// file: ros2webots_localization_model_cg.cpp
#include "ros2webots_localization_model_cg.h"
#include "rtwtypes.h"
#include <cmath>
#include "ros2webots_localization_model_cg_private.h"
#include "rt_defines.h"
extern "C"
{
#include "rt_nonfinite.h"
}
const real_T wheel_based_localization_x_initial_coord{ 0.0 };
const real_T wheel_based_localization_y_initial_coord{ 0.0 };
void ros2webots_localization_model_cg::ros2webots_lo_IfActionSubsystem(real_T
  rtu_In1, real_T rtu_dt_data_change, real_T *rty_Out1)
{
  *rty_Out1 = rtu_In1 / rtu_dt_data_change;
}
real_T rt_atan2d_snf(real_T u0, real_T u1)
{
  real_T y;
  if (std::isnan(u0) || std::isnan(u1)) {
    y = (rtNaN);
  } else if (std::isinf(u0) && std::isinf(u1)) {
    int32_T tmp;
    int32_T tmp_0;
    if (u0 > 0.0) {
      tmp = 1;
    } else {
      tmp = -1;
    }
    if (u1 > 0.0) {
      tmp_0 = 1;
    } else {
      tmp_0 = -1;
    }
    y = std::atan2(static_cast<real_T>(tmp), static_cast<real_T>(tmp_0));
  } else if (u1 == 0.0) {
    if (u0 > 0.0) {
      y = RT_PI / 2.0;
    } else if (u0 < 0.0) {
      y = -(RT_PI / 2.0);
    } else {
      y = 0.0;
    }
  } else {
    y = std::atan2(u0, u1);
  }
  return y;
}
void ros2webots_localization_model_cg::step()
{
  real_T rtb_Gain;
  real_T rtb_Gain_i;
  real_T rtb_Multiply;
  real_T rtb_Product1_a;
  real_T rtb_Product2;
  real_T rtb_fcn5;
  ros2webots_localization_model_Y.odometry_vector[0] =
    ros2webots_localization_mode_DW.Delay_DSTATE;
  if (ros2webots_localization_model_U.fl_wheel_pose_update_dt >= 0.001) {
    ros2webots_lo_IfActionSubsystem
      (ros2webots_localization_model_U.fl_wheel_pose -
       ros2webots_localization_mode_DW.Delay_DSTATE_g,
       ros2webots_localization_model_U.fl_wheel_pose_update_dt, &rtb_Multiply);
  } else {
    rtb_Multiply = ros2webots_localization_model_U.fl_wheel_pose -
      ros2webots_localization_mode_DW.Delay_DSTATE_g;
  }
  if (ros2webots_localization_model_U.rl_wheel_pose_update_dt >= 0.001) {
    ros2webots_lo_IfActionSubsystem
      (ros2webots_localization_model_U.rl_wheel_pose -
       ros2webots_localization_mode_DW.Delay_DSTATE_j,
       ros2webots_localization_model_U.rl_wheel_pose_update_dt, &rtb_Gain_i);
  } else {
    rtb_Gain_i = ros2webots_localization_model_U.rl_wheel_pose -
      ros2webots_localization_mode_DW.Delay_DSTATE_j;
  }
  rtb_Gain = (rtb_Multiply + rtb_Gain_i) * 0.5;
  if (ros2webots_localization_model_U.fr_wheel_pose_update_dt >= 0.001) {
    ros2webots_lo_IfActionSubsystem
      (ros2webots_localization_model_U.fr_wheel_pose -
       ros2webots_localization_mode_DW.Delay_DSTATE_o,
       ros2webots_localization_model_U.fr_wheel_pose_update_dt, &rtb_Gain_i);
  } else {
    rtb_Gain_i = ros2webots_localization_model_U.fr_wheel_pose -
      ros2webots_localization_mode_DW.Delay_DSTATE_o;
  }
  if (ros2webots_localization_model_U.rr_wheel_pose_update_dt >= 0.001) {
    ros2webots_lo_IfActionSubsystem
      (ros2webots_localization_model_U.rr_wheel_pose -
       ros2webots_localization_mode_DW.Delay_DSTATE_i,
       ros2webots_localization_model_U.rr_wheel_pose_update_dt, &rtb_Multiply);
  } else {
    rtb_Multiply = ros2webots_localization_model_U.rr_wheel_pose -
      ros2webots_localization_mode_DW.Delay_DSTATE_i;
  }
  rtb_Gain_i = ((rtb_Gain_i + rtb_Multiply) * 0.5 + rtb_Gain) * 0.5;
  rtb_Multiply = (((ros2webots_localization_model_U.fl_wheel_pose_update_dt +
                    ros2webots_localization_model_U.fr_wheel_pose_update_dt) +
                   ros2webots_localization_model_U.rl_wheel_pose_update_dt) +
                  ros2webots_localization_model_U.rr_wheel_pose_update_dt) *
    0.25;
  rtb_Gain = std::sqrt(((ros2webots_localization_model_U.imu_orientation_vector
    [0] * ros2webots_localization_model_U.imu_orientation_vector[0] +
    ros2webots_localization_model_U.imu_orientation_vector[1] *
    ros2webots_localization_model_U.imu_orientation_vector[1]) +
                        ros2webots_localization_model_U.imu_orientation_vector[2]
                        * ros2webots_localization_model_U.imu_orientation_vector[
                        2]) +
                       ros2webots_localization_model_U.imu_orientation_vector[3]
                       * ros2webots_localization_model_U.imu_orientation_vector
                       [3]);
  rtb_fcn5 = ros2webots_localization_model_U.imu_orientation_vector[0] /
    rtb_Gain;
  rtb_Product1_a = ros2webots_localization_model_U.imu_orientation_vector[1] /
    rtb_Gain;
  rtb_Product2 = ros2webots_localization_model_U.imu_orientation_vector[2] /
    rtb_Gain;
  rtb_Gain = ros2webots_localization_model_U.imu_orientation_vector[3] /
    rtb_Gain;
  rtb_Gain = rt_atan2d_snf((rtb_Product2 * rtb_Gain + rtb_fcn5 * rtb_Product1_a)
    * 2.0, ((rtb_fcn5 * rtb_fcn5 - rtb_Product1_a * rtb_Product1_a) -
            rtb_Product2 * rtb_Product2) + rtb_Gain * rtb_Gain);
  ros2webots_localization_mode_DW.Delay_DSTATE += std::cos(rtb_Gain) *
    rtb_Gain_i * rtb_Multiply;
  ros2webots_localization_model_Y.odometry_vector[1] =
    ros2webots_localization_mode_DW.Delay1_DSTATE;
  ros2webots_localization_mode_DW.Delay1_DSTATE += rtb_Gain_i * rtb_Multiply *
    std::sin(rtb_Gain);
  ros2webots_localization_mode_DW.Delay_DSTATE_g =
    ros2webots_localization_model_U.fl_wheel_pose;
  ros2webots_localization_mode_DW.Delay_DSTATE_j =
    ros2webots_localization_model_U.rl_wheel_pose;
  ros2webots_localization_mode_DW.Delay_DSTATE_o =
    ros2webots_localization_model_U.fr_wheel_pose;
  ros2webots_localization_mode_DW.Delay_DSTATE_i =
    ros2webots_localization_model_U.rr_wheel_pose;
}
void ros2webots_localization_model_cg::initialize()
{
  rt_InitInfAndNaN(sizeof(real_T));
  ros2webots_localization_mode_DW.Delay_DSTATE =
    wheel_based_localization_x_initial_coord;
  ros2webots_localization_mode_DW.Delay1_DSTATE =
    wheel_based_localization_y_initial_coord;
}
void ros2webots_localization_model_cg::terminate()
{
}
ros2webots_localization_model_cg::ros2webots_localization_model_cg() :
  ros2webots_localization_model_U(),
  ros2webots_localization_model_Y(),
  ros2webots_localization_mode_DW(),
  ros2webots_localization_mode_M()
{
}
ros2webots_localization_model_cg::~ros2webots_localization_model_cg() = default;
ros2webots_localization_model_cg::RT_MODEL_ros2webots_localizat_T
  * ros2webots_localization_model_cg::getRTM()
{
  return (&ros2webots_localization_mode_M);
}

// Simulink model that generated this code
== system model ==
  imu_orientation_vector : Inport
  Inport#1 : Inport
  Inport#2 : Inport
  fl_wheel_pose : Inport
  fr_wheel_pose : Inport
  rl_wheel_pose : Inport
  rr_wheel_pose : Inport
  fl_wheel_pose_update_dt : Inport
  fr_wheel_pose_update_dt : Inport
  rl_wheel_pose_update_dt : Inport
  rr_wheel_pose_update_dt : Inport
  odometry_vector : Outport  <- 1: Concatenate#1
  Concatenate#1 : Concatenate  <- 1: Delay, 2: Delay1
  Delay : Delay  DelayLength=1  InitialCondition=wheel_based_localization_x_initial_coord  <- 1: Sum#1
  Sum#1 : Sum  Inputs=++  <- 1: Product#1, 2: Delay
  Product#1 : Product  Inputs=3  <- 1: Trigonometry#1, 2: Gain, 3: Multiply
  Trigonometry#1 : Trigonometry  Operator=cos  <- 1: Selector#1
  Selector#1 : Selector  Indices=3  <- 1: QuaternionstoRotationAngles#1
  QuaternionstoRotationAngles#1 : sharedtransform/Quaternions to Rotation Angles  <- 1: Concatenate#2
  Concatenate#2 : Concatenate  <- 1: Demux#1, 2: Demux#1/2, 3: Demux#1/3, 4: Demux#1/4
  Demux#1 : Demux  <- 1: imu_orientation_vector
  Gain : Gain  Gain=1/2  <- 1: Sum#2
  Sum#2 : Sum  Inputs=++  <- 1: Gain#1, 2: Gain#2
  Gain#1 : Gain  Gain=1/2  <- 1: Sum#3
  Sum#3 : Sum  Inputs=++  <- 1: Merge#1, 2: Merge#2
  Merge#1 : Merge  <- 1: IfActionSubsystem, 2: Subsystem#1
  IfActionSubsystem : Subsystem  <- 1: Sum#4, 2: fl_wheel_pose_update_dt, Action: If#1
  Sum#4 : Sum  Inputs=+-  <- 1: fl_wheel_pose, 2: Delay#1
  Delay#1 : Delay  DelayLength=1  <- 1: fl_wheel_pose
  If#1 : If  IfExpression=u1 >= manual_derivative_dt_threshold  <- 1: fl_wheel_pose_update_dt
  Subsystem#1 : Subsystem  <- 1: Sum#4, Action: If#1/2
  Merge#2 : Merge  <- 1: Subsystem#2, 2: Subsystem#3
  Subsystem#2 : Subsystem  <- 1: Sum#5, 2: rl_wheel_pose_update_dt, Action: If#2
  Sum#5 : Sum  Inputs=+-  <- 1: rl_wheel_pose, 2: Delay#2
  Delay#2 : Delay  DelayLength=1  <- 1: rl_wheel_pose
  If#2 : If  IfExpression=u1 >= manual_derivative_dt_threshold  <- 1: rl_wheel_pose_update_dt
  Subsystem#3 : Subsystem  <- 1: Sum#5, Action: If#2/2
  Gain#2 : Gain  Gain=1/2  <- 1: Sum#6
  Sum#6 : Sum  Inputs=++  <- 1: Merge#3, 2: Merge#4
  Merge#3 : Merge  <- 1: Subsystem#4, 2: Subsystem#5
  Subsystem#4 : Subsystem  <- 1: Sum#7, 2: fr_wheel_pose_update_dt, Action: If#3
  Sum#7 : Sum  Inputs=+-  <- 1: fr_wheel_pose, 2: Delay#3
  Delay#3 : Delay  DelayLength=1  <- 1: fr_wheel_pose
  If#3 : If  IfExpression=u1 >= manual_derivative_dt_threshold  <- 1: fr_wheel_pose_update_dt
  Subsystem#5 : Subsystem  <- 1: Sum#7, Action: If#3/2
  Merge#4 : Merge  <- 1: Subsystem#6, 2: Subsystem#7
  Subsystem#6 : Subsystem  <- 1: Sum#8, 2: rr_wheel_pose_update_dt, Action: If#4
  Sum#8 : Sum  Inputs=+-  <- 1: rr_wheel_pose, 2: Delay#4
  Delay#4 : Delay  DelayLength=1  <- 1: rr_wheel_pose
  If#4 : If  IfExpression=u1 >= manual_derivative_dt_threshold  <- 1: rr_wheel_pose_update_dt
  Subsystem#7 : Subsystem  <- 1: Sum#8, Action: If#4/2
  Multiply : Gain  Gain=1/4  <- 1: Sum#9
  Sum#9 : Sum  Inputs=++++  <- 1: fl_wheel_pose_update_dt, 2: fr_wheel_pose_update_dt, 3: rl_wheel_pose_update_dt, 4: rr_wheel_pose_update_dt
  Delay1 : Delay  DelayLength=1  InitialCondition=wheel_based_localization_y_initial_coord  <- 1: Sum#10
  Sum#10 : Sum  Inputs=++  <- 1: Product1, 2: Delay1
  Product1 : Product  Inputs=3  <- 1: Gain, 2: Multiply, 3: Trigonometry#2
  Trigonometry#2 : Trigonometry  <- 1: Selector#1
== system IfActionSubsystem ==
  In1 : Inport
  dt_data_change : Inport
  ActionPort#1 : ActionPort
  Out1 : Outport  <- 1: Product#2
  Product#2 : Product  Inputs=*/  <- 1: In1, 2: dt_data_change
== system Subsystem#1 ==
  Inport#3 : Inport
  ActionPort#2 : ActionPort
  Outport#1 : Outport  <- 1: Inport#3
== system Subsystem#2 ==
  Inport#4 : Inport
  Inport#5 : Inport
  ActionPort#3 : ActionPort
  Outport#2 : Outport  <- 1: Product#3
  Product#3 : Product  Inputs=*/  <- 1: Inport#4, 2: Inport#5
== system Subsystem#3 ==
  Inport#6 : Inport
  ActionPort#4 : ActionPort
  Outport#3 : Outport  <- 1: Inport#6
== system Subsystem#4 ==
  Inport#7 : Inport
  Inport#8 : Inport
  ActionPort#5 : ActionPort
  Outport#4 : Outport  <- 1: Product#4
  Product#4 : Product  Inputs=*/  <- 1: Inport#7, 2: Inport#8
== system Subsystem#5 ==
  Inport#9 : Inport
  ActionPort#6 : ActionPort
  Outport#5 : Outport  <- 1: Inport#9
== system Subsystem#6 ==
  Inport#10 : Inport
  Inport#11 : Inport
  ActionPort#7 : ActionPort
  Outport#6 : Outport  <- 1: Product#5
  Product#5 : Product  Inputs=*/  <- 1: Inport#10, 2: Inport#11
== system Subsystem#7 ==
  Inport#12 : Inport
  ActionPort#8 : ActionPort
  Outport#7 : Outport  <- 1: Inport#12
